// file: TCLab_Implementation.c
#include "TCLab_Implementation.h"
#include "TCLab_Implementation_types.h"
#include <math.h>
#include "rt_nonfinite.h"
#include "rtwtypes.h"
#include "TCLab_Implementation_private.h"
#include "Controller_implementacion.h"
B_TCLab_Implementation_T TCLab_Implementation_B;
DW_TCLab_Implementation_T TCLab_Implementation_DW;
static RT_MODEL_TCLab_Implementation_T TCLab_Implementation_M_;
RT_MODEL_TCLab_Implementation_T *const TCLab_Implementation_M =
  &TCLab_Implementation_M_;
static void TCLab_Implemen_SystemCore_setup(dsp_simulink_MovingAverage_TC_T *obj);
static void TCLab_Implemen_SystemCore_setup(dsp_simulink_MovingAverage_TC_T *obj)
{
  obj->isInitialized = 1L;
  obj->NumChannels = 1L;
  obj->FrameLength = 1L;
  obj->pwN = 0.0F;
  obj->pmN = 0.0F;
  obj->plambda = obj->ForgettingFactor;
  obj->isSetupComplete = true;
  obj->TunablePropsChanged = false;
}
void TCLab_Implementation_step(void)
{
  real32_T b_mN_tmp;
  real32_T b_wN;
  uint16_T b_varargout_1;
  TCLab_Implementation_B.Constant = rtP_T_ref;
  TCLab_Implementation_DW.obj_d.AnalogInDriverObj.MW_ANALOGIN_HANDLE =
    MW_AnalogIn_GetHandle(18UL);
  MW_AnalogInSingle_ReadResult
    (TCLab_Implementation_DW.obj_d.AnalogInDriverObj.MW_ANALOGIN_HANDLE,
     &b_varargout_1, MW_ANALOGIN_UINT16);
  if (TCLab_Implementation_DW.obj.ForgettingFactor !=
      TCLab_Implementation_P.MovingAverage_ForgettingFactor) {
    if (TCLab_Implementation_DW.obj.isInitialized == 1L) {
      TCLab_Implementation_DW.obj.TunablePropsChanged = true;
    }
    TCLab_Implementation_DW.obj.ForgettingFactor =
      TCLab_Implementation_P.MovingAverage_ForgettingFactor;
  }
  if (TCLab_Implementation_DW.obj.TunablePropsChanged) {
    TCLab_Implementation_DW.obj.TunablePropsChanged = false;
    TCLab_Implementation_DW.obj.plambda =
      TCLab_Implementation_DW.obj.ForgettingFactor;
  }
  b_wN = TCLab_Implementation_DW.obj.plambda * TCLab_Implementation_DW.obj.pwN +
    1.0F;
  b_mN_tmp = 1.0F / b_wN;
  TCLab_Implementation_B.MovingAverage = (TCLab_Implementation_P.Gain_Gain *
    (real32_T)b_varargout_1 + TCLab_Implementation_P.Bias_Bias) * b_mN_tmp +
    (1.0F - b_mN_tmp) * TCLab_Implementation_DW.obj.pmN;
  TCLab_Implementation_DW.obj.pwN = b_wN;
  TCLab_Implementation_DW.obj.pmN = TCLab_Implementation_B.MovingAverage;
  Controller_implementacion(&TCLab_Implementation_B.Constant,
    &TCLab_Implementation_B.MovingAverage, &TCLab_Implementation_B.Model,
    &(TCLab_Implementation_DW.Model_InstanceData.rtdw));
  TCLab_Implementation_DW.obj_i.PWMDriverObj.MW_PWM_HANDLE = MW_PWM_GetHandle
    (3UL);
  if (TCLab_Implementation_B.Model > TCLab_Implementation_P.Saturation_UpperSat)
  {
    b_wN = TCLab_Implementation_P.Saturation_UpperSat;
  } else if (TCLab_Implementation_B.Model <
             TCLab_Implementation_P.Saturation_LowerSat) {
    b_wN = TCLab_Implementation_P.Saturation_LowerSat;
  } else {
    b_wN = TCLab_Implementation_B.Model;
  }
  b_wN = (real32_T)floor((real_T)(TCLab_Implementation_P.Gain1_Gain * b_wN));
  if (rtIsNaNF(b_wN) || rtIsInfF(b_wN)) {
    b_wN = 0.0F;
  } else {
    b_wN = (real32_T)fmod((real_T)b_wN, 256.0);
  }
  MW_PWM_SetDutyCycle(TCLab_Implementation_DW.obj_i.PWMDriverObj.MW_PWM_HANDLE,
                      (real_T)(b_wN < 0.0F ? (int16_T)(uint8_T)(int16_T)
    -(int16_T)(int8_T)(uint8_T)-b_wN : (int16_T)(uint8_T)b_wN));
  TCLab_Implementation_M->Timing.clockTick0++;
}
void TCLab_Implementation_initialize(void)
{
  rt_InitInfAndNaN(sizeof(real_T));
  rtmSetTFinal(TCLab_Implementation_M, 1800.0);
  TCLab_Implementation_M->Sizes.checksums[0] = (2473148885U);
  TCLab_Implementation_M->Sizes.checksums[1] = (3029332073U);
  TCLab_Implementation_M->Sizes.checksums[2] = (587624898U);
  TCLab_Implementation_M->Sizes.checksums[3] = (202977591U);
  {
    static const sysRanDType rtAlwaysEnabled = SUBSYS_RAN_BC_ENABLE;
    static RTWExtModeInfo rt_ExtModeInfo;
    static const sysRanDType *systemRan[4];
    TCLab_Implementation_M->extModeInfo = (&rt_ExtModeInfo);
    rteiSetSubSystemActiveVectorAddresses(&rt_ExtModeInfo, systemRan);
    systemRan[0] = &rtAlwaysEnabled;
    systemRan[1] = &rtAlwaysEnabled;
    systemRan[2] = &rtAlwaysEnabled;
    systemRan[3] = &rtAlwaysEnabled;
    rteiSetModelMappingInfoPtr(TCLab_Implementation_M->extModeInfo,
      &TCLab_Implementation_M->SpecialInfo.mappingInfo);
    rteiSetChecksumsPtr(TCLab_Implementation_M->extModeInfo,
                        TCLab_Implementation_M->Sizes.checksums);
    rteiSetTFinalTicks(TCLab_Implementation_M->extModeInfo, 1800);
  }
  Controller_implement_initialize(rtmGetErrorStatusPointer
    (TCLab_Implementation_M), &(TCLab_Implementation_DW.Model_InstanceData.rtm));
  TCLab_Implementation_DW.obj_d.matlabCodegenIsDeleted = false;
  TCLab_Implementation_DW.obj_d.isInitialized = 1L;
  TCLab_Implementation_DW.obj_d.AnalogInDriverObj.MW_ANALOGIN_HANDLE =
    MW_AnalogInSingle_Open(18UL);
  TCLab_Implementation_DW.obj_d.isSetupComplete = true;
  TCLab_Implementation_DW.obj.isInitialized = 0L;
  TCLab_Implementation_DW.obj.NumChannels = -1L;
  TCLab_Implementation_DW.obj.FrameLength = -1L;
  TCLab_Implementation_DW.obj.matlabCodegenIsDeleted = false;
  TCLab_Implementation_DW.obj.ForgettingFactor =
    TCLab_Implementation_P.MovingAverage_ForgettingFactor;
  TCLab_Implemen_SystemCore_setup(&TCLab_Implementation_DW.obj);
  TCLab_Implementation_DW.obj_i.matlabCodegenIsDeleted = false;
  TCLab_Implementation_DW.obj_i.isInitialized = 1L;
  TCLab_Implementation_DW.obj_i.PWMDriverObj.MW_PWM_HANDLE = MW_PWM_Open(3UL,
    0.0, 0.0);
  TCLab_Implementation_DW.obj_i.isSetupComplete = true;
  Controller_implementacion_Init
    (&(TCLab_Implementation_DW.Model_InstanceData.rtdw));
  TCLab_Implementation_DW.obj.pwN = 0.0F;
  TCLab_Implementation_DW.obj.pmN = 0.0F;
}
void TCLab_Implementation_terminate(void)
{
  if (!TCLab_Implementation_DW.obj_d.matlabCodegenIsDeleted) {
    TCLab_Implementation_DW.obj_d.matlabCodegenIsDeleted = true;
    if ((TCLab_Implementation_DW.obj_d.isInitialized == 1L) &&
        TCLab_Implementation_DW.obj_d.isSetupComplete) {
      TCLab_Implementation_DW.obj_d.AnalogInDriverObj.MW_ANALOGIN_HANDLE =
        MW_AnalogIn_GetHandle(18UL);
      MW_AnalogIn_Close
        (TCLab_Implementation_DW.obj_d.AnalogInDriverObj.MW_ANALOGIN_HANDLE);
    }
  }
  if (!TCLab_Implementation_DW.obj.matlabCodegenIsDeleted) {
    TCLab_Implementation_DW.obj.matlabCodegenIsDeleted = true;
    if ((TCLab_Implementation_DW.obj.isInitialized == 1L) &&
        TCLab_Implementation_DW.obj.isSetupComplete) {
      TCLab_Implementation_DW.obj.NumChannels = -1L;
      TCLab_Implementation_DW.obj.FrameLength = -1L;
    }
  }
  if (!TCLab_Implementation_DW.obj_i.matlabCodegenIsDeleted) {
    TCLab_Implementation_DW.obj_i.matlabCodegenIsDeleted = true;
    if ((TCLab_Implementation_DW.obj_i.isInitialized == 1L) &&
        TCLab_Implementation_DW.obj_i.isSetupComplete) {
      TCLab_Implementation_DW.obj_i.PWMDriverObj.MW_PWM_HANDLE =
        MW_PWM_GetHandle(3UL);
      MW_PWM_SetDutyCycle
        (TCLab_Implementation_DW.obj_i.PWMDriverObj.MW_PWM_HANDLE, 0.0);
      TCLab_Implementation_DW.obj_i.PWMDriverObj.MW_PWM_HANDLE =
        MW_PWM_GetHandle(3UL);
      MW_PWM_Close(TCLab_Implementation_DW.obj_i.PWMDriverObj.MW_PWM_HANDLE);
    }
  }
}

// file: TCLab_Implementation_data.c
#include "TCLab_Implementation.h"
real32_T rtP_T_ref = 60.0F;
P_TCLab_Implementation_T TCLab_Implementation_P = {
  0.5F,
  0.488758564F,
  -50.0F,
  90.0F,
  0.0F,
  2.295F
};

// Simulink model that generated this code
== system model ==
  PWM#1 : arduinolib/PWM  pinNumber=3  <- 1: DataTypeConversion#1
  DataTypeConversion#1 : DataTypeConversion  <- 1: Gain1
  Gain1 : Gain  Gain=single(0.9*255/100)  <- 1: Saturation
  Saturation : Saturate  UpperLimit=90  LowerLimit=0  <- 1: Model
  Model : ModelReference  <- 1: Constant, 2: MovingAverage
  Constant : Constant  Value=T_ref
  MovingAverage : dspstat3/Moving Average  <- 1: Bias
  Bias : Bias  Bias=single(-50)  <- 1: Gain
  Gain : Gain  Gain=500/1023  <- 1: DataTypeConversion#2
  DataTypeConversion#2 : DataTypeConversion  <- 1: AnalogInput#1
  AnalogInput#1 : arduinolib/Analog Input  pinNumber=0
